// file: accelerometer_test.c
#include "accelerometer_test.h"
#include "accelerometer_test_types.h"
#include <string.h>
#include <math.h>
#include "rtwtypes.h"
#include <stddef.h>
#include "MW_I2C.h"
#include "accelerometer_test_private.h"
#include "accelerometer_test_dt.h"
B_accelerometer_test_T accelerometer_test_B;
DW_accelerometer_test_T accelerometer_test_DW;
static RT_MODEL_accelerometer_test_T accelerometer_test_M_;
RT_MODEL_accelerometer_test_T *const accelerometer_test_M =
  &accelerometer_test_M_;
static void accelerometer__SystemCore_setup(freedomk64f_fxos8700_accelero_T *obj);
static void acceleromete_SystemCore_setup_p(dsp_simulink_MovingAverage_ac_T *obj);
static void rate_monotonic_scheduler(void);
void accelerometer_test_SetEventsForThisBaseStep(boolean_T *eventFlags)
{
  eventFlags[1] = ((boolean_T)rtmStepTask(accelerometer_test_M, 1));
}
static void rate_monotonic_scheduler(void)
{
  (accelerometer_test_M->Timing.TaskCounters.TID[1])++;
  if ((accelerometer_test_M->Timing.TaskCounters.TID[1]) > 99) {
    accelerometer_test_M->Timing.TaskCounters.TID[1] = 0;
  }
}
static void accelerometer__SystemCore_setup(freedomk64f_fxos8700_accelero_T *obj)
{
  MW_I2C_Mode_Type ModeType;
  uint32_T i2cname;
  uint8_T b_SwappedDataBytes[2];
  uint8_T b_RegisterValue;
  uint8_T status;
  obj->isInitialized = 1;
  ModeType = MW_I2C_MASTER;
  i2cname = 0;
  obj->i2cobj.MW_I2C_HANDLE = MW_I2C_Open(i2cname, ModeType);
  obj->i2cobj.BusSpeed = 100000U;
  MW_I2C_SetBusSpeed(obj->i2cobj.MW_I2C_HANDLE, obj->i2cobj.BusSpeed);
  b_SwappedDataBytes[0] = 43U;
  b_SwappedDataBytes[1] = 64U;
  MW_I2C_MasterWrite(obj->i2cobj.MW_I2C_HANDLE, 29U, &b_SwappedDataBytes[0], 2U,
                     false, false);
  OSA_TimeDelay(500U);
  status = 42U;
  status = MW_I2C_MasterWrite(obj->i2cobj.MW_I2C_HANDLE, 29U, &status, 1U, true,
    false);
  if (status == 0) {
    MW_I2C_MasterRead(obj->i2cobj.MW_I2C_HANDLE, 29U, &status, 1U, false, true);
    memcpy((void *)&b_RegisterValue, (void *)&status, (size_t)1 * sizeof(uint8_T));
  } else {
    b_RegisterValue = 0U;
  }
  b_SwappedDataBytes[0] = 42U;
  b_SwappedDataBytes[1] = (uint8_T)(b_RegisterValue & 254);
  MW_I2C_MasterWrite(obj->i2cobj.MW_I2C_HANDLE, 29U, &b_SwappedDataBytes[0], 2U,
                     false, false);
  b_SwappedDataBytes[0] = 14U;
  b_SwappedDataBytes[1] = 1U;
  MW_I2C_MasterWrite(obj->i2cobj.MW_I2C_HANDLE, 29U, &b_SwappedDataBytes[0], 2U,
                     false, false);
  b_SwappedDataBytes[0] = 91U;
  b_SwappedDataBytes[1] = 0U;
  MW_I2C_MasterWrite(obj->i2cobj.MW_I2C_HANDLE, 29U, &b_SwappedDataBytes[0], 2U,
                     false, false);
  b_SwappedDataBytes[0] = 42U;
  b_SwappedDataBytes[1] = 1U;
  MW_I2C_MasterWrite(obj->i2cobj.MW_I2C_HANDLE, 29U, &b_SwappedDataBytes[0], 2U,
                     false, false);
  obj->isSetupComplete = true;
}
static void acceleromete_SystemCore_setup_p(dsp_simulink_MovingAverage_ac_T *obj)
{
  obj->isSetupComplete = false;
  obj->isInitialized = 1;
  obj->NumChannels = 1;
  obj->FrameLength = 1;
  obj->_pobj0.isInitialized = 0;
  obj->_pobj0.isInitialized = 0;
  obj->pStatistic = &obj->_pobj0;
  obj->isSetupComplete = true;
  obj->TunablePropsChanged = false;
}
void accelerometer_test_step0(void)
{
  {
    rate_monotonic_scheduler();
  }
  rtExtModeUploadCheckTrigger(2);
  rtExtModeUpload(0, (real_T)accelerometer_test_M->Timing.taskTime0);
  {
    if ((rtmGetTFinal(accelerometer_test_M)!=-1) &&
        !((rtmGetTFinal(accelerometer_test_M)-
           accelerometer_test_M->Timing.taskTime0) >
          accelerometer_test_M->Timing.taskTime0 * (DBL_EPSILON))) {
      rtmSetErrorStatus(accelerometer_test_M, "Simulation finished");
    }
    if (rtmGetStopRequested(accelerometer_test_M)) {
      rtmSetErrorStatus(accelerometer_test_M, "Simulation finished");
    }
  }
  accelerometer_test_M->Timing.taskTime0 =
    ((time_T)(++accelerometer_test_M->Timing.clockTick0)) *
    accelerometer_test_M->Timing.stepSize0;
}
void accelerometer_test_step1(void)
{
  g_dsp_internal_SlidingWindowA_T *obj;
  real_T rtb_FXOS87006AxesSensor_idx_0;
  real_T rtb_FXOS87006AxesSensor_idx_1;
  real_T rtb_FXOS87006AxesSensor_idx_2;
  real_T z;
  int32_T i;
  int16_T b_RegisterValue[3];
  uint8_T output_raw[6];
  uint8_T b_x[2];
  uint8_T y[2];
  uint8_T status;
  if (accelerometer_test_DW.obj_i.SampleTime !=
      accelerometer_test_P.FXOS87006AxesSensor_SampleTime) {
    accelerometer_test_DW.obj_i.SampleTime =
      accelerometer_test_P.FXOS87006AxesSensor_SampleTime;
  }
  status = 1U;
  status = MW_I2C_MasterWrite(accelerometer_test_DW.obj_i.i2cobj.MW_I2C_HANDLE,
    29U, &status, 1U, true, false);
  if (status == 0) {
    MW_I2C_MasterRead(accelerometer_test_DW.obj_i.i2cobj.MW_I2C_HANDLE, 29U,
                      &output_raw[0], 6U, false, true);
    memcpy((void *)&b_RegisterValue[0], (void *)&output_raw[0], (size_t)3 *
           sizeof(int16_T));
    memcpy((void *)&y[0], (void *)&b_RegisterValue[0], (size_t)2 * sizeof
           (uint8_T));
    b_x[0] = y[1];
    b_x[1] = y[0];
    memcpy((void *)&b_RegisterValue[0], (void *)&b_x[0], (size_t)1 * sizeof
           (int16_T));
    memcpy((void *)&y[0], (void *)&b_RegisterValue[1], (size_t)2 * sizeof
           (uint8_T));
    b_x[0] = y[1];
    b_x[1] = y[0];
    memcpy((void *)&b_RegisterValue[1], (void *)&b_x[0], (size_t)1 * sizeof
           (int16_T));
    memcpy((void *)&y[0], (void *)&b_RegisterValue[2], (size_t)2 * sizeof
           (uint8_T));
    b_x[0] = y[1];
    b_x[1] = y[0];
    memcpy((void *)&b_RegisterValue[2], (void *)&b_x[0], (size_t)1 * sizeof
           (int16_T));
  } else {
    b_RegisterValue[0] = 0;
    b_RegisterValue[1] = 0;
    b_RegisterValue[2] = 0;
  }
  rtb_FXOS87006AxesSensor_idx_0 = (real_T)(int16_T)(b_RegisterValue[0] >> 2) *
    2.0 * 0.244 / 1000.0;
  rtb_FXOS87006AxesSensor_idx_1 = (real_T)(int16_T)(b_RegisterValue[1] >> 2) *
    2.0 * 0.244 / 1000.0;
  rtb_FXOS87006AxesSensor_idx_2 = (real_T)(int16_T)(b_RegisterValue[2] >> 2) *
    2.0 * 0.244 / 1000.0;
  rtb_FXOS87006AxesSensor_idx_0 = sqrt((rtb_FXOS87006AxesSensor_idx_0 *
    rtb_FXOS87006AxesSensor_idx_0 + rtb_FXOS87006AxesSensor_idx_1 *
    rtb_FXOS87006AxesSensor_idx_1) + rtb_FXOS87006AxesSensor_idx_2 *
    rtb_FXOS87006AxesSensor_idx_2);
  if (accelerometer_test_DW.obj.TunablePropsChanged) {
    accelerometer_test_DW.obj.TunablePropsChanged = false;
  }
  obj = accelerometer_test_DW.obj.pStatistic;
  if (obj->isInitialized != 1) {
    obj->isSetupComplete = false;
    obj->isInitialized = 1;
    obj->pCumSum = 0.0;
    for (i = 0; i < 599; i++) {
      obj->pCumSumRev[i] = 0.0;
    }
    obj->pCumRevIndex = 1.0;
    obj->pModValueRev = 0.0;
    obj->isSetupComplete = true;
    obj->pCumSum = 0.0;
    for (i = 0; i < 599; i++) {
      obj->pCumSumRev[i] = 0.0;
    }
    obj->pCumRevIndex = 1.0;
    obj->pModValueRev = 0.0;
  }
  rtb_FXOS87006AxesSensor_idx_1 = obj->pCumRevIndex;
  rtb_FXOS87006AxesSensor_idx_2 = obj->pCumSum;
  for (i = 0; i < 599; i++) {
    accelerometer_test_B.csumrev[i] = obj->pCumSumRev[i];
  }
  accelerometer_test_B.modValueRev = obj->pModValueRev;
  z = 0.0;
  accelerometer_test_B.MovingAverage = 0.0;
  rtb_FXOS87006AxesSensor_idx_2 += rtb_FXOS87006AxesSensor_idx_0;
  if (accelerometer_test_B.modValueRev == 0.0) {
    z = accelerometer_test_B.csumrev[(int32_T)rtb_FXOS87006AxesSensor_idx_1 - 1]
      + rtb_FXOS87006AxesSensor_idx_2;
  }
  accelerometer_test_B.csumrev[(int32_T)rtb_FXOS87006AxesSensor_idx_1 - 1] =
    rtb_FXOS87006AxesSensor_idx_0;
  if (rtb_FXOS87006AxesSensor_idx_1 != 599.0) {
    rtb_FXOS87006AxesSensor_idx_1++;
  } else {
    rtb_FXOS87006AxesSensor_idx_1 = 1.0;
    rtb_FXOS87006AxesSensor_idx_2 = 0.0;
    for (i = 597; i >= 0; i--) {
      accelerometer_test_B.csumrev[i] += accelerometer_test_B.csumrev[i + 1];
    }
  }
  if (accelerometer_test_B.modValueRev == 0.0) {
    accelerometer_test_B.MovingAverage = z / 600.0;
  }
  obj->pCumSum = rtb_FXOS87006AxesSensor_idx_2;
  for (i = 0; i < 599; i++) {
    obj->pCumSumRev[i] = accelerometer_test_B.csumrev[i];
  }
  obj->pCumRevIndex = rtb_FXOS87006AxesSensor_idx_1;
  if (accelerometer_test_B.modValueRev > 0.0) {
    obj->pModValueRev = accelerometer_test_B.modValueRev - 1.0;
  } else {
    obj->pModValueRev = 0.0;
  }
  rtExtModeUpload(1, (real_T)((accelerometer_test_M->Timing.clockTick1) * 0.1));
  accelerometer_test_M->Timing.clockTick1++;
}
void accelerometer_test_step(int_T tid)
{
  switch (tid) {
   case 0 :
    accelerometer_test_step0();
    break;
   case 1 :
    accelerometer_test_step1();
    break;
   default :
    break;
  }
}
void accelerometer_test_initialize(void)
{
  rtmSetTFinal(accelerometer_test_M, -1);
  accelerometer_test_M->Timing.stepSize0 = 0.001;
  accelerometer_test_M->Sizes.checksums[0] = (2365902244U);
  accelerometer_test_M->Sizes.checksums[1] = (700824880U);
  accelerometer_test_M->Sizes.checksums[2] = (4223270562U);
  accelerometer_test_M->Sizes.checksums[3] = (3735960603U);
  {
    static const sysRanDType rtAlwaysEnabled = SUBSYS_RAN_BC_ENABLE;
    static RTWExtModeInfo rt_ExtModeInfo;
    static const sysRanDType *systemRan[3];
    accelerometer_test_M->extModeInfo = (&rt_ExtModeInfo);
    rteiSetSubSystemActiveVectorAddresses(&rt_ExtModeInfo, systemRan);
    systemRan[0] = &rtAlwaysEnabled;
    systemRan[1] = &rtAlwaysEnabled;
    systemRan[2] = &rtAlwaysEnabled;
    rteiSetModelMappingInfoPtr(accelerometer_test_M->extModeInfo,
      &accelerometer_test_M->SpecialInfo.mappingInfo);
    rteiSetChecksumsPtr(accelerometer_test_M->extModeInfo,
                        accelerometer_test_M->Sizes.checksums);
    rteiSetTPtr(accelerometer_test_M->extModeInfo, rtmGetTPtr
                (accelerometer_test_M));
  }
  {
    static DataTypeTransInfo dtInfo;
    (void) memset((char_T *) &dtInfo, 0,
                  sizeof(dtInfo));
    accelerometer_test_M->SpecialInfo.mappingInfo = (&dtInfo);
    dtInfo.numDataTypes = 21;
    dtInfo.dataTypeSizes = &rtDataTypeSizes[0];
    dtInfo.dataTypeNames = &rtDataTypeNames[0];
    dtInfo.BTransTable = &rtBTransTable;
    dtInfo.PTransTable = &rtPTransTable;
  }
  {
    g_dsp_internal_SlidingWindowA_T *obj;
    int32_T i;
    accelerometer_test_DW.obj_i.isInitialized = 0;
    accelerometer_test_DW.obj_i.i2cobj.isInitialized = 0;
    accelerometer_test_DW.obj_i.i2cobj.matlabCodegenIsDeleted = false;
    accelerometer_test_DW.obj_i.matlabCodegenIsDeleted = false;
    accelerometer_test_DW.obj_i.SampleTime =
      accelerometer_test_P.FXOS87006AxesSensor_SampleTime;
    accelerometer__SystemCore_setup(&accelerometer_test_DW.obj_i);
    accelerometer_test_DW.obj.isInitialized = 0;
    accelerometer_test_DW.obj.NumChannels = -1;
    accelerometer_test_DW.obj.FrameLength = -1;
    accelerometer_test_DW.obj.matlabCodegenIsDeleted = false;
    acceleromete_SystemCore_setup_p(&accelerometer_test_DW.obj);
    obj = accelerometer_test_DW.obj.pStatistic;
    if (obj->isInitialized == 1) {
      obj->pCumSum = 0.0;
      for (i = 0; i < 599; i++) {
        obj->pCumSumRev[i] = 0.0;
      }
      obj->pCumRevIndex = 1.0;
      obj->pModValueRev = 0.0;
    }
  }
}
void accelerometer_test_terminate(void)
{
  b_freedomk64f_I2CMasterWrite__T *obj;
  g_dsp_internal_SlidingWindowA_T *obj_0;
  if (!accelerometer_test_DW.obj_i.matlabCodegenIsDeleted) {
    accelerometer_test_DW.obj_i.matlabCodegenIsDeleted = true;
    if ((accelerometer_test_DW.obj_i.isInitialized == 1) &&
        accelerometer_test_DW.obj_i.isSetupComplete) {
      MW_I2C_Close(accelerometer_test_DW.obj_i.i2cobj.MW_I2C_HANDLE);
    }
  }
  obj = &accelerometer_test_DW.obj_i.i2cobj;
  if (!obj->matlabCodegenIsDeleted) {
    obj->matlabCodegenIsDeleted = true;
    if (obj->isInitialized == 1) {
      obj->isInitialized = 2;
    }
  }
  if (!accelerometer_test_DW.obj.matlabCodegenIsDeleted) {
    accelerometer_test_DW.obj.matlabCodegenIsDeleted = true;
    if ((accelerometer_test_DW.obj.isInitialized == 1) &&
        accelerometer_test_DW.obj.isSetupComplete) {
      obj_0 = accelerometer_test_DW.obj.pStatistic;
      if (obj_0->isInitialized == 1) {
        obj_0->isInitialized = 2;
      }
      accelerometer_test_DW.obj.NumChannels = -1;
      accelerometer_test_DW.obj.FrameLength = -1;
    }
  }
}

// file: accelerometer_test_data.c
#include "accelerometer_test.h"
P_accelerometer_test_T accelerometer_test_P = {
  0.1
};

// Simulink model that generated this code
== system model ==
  MovingAverage : dspstat3/Moving Average  <- 1: Sqrt#1
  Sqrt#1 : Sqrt  <- 1: Sum#1
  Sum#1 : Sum  <- 1: Sum#2, 2: Math#1
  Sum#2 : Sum  <- 1: Math#2, 2: Math#3
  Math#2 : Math  Operator=magnitude^2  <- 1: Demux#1
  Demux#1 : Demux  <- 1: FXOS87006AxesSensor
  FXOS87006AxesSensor : frdmk64flib/FXOS8700 6-Axes Sensor
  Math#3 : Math  Operator=magnitude^2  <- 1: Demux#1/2
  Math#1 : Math  Operator=magnitude^2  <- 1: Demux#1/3
